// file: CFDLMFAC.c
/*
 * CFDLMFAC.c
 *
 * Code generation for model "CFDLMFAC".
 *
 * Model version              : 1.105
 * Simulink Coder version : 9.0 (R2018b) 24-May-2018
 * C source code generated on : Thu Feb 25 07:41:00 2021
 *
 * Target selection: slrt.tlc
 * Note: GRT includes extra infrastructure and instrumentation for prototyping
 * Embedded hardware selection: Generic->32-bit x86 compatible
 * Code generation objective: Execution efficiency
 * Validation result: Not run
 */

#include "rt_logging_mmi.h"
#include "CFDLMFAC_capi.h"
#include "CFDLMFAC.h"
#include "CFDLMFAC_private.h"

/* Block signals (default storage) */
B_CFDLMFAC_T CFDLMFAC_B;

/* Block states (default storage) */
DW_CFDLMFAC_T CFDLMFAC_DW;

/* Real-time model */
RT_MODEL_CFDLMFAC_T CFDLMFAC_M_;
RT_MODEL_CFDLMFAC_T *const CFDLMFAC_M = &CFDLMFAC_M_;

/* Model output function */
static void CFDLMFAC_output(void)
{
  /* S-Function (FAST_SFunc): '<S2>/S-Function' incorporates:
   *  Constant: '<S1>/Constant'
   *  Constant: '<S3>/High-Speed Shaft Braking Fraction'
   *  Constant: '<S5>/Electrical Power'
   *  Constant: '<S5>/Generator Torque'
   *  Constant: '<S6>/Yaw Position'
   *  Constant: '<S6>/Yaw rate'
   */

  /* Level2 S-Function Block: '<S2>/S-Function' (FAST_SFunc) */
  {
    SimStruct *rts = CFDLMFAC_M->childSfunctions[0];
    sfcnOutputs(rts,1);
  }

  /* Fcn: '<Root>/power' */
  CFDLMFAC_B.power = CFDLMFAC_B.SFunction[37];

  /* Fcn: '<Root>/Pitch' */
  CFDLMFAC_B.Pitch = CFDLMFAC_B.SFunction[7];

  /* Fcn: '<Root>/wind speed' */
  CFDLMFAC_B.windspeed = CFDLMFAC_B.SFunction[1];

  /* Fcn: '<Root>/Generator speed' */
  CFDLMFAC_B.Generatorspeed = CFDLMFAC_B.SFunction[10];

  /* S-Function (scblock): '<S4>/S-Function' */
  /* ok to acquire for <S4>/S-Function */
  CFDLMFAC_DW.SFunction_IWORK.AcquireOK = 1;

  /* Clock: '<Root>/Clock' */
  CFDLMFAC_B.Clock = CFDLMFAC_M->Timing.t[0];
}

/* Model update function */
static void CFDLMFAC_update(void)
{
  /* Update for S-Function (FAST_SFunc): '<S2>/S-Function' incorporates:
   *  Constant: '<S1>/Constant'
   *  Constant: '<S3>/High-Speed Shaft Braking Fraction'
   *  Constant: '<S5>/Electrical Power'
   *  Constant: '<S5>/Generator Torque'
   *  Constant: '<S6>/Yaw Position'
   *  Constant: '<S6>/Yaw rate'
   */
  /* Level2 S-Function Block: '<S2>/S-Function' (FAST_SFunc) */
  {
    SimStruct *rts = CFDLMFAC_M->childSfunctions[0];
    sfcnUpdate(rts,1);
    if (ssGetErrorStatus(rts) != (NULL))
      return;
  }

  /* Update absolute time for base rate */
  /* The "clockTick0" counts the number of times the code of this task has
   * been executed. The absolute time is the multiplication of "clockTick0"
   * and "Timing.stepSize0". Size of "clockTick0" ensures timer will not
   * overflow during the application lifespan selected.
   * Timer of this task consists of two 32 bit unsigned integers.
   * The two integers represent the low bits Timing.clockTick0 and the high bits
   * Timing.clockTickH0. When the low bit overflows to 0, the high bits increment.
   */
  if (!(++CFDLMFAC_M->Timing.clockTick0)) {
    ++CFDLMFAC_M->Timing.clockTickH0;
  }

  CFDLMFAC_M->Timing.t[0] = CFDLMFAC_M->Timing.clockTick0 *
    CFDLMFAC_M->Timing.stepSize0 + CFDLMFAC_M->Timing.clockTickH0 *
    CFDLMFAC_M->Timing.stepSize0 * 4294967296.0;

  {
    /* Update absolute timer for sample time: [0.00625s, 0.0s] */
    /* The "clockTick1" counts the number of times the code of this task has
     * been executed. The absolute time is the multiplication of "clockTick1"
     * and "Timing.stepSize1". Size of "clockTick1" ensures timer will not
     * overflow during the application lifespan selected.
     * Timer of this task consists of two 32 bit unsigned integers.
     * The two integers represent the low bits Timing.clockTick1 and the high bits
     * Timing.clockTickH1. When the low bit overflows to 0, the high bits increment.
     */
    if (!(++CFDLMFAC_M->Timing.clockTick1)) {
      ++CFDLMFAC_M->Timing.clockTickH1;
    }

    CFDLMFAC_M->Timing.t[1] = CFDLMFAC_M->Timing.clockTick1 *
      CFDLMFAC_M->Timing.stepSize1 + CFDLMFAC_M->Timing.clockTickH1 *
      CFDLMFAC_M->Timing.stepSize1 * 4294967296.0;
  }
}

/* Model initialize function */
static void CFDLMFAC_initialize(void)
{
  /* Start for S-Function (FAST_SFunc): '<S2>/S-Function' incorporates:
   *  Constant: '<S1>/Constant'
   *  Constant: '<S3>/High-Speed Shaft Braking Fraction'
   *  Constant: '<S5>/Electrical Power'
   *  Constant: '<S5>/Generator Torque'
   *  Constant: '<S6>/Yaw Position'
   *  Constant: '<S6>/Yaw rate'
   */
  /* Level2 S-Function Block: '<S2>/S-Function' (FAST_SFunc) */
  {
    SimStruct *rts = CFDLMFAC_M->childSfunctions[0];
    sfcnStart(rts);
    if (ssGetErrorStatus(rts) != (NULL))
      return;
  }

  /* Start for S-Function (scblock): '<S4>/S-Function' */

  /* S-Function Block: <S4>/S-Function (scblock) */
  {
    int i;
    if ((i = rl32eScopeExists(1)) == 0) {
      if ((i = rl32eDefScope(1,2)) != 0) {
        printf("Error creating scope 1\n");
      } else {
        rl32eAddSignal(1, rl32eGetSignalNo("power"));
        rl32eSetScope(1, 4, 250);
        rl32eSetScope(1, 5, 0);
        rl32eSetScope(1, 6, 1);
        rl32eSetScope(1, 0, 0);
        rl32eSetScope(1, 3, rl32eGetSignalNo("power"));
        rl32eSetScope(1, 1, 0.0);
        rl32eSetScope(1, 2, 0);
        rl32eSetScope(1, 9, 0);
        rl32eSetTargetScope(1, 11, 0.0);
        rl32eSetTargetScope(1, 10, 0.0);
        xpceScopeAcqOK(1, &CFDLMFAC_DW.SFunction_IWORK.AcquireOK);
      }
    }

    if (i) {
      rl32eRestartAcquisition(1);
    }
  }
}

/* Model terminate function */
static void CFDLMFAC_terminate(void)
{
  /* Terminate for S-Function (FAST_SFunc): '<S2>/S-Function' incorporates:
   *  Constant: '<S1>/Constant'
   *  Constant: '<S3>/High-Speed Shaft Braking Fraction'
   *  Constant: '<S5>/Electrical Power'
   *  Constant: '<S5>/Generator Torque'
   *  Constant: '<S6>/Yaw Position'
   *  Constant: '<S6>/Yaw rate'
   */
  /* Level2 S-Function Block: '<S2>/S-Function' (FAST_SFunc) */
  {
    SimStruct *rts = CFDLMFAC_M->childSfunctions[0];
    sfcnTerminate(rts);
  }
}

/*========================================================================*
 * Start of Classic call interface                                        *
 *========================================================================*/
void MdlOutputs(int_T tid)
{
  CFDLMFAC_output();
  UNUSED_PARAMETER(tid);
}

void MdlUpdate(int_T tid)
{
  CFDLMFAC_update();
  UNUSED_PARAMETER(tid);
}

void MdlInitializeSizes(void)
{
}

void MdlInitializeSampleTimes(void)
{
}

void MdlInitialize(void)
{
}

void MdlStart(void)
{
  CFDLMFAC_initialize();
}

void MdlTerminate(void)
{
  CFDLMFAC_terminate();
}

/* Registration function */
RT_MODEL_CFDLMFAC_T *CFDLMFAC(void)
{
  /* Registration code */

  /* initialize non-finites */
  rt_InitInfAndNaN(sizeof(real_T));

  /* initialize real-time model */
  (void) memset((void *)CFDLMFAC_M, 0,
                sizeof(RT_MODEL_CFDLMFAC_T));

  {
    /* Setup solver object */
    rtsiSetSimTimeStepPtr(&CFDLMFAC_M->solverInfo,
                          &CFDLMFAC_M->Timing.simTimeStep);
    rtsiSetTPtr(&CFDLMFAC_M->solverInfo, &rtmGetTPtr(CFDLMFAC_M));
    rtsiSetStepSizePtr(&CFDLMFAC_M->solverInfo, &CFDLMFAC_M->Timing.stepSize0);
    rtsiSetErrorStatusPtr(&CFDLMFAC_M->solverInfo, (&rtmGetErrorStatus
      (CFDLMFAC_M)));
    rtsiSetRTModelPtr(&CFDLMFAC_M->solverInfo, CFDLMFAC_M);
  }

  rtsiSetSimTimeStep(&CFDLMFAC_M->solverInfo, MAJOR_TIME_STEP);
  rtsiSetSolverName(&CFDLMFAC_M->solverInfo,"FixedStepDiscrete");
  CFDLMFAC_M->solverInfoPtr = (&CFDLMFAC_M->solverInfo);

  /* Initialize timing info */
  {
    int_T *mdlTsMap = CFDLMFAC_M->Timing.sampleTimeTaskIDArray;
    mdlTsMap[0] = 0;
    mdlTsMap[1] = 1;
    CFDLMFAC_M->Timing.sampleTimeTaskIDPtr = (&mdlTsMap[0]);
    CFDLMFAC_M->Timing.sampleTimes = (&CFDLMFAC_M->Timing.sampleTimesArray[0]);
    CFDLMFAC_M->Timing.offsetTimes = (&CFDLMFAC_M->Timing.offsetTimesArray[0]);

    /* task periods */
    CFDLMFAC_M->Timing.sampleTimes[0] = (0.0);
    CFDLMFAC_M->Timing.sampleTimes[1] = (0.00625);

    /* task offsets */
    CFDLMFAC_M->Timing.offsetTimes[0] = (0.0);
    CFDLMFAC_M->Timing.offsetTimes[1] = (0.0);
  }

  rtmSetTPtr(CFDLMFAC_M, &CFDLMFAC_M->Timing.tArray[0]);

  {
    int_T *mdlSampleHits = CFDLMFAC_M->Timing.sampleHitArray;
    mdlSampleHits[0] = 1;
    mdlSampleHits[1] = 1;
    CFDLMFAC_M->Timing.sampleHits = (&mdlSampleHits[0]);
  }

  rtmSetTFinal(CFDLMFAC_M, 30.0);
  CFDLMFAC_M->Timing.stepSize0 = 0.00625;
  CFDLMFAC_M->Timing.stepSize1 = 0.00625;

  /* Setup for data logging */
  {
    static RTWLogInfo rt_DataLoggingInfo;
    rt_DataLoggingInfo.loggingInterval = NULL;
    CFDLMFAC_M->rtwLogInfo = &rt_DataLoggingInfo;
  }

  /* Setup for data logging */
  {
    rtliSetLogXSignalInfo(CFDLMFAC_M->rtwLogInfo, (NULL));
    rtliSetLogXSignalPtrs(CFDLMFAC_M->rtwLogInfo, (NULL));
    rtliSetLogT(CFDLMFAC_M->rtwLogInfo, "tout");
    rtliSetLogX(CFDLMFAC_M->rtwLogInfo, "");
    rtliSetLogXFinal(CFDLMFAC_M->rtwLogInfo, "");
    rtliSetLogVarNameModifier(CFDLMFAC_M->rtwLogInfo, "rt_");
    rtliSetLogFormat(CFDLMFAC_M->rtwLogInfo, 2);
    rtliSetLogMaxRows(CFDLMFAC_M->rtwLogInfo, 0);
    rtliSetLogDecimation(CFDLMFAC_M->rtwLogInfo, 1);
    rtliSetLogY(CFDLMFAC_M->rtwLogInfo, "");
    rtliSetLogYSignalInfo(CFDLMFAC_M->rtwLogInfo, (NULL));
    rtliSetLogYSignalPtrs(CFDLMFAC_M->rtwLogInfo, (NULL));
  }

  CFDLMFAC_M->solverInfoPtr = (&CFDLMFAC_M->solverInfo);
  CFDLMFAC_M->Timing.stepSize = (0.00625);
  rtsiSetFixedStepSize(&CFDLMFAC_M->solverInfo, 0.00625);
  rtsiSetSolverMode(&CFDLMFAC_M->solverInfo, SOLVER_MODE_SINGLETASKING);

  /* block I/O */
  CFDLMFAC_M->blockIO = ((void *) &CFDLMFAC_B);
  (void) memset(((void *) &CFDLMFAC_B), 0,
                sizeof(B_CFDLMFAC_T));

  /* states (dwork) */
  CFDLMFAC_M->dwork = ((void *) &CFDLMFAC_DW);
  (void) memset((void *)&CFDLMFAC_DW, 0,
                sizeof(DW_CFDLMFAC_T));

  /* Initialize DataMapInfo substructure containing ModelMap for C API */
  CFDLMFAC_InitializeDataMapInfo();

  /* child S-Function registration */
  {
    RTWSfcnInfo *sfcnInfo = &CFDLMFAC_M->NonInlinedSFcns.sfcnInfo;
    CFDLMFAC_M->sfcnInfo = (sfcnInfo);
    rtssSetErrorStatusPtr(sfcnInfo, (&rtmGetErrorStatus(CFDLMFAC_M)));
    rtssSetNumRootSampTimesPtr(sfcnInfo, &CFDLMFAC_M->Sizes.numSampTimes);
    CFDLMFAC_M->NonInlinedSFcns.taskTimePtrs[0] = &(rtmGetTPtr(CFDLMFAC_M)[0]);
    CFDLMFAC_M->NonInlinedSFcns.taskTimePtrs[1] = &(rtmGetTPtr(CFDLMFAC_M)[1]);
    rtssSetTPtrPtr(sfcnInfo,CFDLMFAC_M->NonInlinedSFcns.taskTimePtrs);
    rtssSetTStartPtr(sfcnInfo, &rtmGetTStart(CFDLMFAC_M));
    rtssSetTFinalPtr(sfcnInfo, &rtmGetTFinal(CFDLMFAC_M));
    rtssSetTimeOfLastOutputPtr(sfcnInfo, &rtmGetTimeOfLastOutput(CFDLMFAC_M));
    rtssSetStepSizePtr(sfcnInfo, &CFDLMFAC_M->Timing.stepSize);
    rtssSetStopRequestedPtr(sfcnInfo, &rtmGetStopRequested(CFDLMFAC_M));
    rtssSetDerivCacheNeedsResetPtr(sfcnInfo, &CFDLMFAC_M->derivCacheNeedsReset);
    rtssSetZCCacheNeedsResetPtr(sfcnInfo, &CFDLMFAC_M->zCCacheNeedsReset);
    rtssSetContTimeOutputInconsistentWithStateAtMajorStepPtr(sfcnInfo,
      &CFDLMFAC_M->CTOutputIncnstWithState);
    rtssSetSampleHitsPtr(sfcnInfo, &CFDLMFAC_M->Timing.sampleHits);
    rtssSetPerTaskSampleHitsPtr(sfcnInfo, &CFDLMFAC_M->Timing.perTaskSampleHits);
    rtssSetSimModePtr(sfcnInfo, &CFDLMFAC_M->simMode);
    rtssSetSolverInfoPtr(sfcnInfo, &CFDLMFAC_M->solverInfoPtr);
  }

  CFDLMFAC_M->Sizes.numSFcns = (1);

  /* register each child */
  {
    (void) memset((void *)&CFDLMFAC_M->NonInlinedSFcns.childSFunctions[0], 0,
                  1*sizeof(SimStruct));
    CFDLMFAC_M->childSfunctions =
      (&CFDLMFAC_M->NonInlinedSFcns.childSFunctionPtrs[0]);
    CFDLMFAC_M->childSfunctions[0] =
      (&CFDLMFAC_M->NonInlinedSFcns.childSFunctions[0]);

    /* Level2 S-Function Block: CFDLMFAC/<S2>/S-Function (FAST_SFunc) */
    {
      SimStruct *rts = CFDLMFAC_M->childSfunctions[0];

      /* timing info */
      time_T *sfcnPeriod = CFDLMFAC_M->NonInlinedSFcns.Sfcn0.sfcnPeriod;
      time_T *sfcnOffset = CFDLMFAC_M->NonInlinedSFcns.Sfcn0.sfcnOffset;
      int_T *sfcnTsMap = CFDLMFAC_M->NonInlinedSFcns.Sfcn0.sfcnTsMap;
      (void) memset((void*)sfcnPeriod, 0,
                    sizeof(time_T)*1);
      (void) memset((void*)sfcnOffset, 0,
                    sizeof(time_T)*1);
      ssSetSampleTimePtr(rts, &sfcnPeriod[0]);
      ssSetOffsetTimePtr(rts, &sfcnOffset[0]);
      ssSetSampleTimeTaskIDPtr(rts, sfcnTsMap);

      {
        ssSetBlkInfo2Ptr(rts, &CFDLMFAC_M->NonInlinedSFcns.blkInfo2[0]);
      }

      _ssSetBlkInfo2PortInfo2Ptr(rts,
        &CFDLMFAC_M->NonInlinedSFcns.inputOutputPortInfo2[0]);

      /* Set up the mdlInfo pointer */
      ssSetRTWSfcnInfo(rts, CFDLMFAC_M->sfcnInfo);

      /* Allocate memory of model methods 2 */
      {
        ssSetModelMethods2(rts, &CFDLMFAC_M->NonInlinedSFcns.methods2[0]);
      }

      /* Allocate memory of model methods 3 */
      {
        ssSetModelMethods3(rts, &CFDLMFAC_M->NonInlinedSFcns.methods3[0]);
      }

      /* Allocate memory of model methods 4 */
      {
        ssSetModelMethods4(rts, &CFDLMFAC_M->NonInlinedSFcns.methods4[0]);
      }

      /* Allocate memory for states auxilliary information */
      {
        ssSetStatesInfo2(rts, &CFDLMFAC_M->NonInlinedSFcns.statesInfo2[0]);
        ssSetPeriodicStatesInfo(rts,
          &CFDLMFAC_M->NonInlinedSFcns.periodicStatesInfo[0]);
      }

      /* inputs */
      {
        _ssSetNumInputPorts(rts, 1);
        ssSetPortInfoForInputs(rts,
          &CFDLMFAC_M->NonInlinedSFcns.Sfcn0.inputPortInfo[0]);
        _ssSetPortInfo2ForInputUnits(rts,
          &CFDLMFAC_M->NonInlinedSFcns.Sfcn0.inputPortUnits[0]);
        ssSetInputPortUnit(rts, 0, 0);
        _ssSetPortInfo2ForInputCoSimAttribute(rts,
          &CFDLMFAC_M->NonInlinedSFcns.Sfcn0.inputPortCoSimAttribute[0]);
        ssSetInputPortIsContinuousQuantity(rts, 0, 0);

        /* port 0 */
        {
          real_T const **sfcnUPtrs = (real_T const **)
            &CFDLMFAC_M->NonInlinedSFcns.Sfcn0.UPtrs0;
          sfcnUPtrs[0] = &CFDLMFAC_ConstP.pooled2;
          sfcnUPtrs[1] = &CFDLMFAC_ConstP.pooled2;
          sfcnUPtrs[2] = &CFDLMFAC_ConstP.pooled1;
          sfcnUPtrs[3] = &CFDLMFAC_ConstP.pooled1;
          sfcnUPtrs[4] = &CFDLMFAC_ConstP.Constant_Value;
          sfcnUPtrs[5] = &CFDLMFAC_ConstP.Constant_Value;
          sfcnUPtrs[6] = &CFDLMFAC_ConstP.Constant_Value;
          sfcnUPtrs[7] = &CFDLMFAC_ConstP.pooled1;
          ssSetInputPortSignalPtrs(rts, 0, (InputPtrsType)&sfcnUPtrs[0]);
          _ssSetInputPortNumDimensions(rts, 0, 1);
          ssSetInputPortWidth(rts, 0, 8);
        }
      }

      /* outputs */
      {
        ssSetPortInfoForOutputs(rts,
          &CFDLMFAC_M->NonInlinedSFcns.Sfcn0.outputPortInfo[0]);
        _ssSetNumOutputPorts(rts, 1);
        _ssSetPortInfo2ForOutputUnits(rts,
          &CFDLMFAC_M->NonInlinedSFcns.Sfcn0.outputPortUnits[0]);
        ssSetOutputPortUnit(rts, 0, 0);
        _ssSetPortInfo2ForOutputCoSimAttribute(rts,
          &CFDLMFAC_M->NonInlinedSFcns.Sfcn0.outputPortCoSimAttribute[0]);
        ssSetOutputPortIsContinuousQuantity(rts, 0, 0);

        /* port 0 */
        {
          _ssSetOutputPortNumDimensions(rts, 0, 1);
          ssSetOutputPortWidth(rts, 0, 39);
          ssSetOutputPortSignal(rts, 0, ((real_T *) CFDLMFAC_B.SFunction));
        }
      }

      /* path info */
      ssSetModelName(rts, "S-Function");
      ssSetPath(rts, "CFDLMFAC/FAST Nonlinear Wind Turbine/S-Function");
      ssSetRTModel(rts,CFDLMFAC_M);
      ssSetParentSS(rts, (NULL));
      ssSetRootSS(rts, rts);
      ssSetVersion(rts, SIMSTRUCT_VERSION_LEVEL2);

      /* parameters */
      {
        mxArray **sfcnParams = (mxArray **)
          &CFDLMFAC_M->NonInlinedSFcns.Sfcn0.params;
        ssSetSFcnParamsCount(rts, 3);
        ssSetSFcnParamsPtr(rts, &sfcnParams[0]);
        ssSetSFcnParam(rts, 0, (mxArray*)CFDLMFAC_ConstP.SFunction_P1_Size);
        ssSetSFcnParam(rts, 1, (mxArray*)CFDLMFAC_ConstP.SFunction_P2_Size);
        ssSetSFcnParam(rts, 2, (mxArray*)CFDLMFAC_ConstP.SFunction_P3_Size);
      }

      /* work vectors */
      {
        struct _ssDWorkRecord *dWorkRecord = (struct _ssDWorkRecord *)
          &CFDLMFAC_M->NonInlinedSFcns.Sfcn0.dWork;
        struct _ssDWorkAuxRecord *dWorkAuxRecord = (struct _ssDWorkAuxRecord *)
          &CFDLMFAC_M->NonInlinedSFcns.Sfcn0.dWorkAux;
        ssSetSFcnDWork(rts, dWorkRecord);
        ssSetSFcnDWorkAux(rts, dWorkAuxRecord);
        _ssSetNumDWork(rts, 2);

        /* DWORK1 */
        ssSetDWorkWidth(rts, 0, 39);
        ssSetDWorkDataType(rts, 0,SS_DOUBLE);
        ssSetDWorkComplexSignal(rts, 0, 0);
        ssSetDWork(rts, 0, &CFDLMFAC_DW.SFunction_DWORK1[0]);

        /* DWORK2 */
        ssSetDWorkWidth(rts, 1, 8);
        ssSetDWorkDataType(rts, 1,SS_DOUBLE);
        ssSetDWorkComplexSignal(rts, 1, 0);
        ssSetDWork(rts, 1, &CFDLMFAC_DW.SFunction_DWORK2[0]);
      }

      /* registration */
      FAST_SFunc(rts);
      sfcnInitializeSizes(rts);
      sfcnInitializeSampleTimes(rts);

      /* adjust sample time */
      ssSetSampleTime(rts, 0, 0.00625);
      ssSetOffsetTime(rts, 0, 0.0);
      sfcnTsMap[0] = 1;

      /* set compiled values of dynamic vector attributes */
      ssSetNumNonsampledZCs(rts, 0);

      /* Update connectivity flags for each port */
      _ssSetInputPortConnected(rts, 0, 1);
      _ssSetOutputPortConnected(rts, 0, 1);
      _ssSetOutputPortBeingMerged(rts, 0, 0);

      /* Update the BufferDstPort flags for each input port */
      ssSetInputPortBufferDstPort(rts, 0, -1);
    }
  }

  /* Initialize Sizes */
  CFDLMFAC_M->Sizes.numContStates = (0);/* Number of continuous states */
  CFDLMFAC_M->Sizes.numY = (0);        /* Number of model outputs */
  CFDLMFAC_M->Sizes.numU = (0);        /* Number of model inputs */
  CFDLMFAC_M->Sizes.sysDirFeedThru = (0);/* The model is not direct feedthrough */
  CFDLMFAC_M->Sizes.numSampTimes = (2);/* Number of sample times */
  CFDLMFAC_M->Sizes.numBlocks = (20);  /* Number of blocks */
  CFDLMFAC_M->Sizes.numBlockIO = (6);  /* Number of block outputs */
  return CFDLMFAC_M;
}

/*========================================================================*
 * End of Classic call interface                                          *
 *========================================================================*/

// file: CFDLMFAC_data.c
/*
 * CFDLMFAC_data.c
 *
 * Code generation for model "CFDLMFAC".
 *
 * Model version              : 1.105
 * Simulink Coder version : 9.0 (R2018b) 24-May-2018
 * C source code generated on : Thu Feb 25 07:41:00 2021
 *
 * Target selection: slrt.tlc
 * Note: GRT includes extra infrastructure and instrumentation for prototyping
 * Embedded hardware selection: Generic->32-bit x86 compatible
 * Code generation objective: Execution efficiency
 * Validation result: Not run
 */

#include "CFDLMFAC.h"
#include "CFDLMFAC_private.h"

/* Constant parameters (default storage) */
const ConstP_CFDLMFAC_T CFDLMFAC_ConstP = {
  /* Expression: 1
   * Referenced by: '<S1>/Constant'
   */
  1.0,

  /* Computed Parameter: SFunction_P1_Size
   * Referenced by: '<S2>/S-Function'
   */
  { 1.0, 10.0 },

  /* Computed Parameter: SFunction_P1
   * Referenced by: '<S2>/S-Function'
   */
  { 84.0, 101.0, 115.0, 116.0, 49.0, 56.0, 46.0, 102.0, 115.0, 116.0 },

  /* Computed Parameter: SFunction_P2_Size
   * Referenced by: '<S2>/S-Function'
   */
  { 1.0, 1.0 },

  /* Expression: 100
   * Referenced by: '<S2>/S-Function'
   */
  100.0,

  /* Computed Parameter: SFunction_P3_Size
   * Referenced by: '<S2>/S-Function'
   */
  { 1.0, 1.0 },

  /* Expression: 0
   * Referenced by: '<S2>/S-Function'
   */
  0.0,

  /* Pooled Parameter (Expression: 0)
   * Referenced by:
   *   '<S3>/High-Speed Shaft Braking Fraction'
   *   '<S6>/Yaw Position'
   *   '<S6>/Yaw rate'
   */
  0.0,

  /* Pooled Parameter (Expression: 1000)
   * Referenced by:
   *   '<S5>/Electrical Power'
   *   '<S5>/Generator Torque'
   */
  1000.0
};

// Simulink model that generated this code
simulink model "CFDLMFAC"  (R2018b)
settings: Solver=ode4  StartTime=0.0  StopTime=30  FixedStep=0.00625  RelTol=1e-3  EnableMultiTasking=on
libraries: slrtlib x1

== system CFDLMFAC ==
  Atomic Subsystem : Subsystem  TreatAsAtomicUnit=on
  Clock : Clock
  FAST Nonlinear Wind Turbine : Subsystem  mask(FAST Nonlinear Wind Turbine){}
      mask help: This block contains the FAST S-Function.
      mask init:
      | clear FAST_SFunc
  Generator speed : Fcn  Expr=u(11)
  Genpwr : Scope
  High-Speed Shaft Brake : Subsystem
  Pitch : Fcn  Expr=u(8)
  "Scope " : slrtlib/Displays and Logging/Scope   scopeno=1  scopetype=Target  autostart=on  viewmode=Graphical redraw  formatstr='%15.6f'  grid=on  ylimits=[0,0]  nosamples=250  noprepostsamples=0  interleave=1  triggermode=FreeRun  triggersignal=1  trigsignalfromport=off  triggerlevel=0.0  triggerslope=Either  triggerscope=1  triggersample=0  filename=data.dat  mode=Lazy  writesize=512  autorestart=off  dynamicfilemode=off  maxwritefilesize=512*1024^2
  To Workspace : ToWorkspace  VariableName=Time  SampleTime=-1
  To Workspace1 : ToWorkspace  VariableName=OutData  SampleTime=-1
  Torque Controller : Subsystem
  Yaw Controller : Subsystem
  power : Fcn  Expr=u(38)
  wind speed : Fcn  Expr=u(2)
  wires:
  High-Speed Shaft Brake/1(Out1) -> FAST Nonlinear Wind Turbine/4(High-Speed Shaft Braking Fraction (-))
  FAST Nonlinear Wind Turbine/1(OutData) -> power/1, wind speed/1, Generator speed/1, Pitch/1, To Workspace1/1
  Yaw Controller/1(Out1) -> FAST Nonlinear Wind Turbine/2(Yaw Position (rad) and Rate (rad/s))
  Clock/1 -> To Workspace/1
  Torque Controller/1(Out1) -> FAST Nonlinear Wind Turbine/1(Gen. Torque (Nm) and Power (W))
  power/1 -> "Scope "/1, Genpwr/1
  Atomic Subsystem/1(Out1) -> FAST Nonlinear Wind Turbine/3(Blade Pitch Angles (rad))

== system CFDLMFAC/Atomic Subsystem ==
  Constant : Constant
  Mux : Mux  Inputs=3
  Out1 : Outport
  wires:
  Mux/1 -> Out1/1
  Constant/1 -> Mux/3, Mux/2, Mux/1

== system CFDLMFAC/FAST Nonlinear Wind Turbine ==
  Gen. Torque (Nm) and Power (W) : Inport
  Yaw Position (rad) and Rate (rad/s) : Inport  Port=2
  Blade Pitch Angles (rad) : Inport  Port=3
  High-Speed Shaft Braking Fraction (-) : Inport  Port=4
  Mux1 : Mux
  S-Function : S-Function  FunctionName=FAST_SFunc  Parameters='Test18.fst', 100, 0  SFunctionDeploymentMode=off  EnableBusSupport=off
  Signal Specification1 : SignalSpecification  OutDataTypeStr=double  Dimensions=2
  Signal Specification2 : SignalSpecification  OutDataTypeStr=double  Dimensions=2
  OutData : Outport
  wires:
  Gen. Torque (Nm) and Power (W)/1 -> Signal Specification1/1
  S-Function/1 -> OutData/1
  Mux1/1 -> S-Function/1
  Blade Pitch Angles (rad)/1 -> Mux1/3
  Yaw Position (rad) and Rate (rad/s)/1 -> Signal Specification2/1
  Signal Specification1/1 -> Mux1/1
  Signal Specification2/1 -> Mux1/2
  High-Speed Shaft Braking Fraction (-)/1 -> Mux1/4

== system CFDLMFAC/High-Speed Shaft Brake ==
  High-Speed Shaft Braking Fraction : Constant  Value=0
  Out1 : Outport
  wires:
  High-Speed Shaft Braking Fraction/1 -> Out1/1

== system CFDLMFAC/Torque Controller ==
  Electrical Power : Constant  Value=1000
  Generator Torque : Constant  Value=1000
  Mux : Mux  Inputs=2
  Out1 : Outport
  wires:
  Mux/1 -> Out1/1
  Generator Torque/1 -> Mux/1
  Electrical Power/1 -> Mux/2

== system CFDLMFAC/Yaw Controller ==
  Mux : Mux  Inputs=2
  Yaw Position : Constant  Value=0
  Yaw rate : Constant  Value=0
  Out1 : Outport
  wires:
  Mux/1 -> Out1/1
  Yaw Position/1 -> Mux/1
  Yaw rate/1 -> Mux/2
